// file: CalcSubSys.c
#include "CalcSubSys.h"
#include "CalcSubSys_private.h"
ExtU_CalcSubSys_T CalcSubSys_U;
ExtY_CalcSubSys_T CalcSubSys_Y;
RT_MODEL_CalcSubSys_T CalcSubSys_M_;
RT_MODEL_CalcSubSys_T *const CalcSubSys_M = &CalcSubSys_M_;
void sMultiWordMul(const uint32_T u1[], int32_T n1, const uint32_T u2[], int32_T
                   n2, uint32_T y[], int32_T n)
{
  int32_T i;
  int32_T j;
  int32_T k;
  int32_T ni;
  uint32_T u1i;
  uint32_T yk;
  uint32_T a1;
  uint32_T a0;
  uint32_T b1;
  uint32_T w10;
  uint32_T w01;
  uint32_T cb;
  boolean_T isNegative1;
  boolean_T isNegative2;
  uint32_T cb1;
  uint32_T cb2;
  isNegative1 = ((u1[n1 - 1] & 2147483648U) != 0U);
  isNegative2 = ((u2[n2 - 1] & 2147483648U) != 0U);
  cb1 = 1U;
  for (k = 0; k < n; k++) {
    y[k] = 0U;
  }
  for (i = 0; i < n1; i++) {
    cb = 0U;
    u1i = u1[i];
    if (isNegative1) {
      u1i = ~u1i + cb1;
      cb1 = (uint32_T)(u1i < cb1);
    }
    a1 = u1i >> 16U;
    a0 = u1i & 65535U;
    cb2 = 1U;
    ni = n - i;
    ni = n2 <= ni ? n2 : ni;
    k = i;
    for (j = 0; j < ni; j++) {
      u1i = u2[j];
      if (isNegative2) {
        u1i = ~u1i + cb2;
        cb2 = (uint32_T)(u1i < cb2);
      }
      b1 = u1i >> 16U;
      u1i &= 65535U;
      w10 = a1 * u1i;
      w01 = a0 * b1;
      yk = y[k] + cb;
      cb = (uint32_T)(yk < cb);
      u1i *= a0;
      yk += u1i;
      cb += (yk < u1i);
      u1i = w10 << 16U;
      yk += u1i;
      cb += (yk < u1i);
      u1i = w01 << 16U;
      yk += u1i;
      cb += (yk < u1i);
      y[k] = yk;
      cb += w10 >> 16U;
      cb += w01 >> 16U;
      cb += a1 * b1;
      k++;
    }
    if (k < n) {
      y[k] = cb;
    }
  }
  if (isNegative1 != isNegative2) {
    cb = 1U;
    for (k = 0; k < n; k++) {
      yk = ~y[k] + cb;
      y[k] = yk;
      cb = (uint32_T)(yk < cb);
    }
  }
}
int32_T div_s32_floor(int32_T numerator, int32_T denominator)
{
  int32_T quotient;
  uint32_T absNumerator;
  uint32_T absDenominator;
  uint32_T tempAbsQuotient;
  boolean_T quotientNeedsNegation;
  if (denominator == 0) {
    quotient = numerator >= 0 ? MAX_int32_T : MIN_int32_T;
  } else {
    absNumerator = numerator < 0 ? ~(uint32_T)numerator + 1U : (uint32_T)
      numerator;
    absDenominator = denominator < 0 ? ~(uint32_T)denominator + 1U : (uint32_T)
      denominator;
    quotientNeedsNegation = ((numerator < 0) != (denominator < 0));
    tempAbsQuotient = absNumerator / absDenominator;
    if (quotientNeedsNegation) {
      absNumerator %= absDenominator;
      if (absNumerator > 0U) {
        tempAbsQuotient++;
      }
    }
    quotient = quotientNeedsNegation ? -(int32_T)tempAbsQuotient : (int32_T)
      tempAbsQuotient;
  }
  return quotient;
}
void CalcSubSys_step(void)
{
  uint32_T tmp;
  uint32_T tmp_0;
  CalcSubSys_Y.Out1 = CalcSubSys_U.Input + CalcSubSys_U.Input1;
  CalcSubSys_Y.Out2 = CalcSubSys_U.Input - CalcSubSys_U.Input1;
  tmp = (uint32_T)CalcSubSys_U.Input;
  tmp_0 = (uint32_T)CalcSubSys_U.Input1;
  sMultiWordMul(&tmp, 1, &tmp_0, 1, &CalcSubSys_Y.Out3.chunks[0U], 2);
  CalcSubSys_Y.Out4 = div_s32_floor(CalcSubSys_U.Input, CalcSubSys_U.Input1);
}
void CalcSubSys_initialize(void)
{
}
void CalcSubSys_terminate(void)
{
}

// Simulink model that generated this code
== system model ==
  Input : Inport
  Input1 : Inport
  Out1 : Outport  <- 1: Sum#1
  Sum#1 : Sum  <- 1: Input, 2: Input1
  Out2 : Outport  <- 1: Sum#2
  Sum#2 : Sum  Inputs=+-  <- 1: Input, 2: Input1
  Out3 : Outport  <- 1: Product#1
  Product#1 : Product  <- 1: Input, 2: Input1
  Out4 : Outport  <- 1: Product#2
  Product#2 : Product  Inputs=*/  <- 1: Input, 2: Input1
